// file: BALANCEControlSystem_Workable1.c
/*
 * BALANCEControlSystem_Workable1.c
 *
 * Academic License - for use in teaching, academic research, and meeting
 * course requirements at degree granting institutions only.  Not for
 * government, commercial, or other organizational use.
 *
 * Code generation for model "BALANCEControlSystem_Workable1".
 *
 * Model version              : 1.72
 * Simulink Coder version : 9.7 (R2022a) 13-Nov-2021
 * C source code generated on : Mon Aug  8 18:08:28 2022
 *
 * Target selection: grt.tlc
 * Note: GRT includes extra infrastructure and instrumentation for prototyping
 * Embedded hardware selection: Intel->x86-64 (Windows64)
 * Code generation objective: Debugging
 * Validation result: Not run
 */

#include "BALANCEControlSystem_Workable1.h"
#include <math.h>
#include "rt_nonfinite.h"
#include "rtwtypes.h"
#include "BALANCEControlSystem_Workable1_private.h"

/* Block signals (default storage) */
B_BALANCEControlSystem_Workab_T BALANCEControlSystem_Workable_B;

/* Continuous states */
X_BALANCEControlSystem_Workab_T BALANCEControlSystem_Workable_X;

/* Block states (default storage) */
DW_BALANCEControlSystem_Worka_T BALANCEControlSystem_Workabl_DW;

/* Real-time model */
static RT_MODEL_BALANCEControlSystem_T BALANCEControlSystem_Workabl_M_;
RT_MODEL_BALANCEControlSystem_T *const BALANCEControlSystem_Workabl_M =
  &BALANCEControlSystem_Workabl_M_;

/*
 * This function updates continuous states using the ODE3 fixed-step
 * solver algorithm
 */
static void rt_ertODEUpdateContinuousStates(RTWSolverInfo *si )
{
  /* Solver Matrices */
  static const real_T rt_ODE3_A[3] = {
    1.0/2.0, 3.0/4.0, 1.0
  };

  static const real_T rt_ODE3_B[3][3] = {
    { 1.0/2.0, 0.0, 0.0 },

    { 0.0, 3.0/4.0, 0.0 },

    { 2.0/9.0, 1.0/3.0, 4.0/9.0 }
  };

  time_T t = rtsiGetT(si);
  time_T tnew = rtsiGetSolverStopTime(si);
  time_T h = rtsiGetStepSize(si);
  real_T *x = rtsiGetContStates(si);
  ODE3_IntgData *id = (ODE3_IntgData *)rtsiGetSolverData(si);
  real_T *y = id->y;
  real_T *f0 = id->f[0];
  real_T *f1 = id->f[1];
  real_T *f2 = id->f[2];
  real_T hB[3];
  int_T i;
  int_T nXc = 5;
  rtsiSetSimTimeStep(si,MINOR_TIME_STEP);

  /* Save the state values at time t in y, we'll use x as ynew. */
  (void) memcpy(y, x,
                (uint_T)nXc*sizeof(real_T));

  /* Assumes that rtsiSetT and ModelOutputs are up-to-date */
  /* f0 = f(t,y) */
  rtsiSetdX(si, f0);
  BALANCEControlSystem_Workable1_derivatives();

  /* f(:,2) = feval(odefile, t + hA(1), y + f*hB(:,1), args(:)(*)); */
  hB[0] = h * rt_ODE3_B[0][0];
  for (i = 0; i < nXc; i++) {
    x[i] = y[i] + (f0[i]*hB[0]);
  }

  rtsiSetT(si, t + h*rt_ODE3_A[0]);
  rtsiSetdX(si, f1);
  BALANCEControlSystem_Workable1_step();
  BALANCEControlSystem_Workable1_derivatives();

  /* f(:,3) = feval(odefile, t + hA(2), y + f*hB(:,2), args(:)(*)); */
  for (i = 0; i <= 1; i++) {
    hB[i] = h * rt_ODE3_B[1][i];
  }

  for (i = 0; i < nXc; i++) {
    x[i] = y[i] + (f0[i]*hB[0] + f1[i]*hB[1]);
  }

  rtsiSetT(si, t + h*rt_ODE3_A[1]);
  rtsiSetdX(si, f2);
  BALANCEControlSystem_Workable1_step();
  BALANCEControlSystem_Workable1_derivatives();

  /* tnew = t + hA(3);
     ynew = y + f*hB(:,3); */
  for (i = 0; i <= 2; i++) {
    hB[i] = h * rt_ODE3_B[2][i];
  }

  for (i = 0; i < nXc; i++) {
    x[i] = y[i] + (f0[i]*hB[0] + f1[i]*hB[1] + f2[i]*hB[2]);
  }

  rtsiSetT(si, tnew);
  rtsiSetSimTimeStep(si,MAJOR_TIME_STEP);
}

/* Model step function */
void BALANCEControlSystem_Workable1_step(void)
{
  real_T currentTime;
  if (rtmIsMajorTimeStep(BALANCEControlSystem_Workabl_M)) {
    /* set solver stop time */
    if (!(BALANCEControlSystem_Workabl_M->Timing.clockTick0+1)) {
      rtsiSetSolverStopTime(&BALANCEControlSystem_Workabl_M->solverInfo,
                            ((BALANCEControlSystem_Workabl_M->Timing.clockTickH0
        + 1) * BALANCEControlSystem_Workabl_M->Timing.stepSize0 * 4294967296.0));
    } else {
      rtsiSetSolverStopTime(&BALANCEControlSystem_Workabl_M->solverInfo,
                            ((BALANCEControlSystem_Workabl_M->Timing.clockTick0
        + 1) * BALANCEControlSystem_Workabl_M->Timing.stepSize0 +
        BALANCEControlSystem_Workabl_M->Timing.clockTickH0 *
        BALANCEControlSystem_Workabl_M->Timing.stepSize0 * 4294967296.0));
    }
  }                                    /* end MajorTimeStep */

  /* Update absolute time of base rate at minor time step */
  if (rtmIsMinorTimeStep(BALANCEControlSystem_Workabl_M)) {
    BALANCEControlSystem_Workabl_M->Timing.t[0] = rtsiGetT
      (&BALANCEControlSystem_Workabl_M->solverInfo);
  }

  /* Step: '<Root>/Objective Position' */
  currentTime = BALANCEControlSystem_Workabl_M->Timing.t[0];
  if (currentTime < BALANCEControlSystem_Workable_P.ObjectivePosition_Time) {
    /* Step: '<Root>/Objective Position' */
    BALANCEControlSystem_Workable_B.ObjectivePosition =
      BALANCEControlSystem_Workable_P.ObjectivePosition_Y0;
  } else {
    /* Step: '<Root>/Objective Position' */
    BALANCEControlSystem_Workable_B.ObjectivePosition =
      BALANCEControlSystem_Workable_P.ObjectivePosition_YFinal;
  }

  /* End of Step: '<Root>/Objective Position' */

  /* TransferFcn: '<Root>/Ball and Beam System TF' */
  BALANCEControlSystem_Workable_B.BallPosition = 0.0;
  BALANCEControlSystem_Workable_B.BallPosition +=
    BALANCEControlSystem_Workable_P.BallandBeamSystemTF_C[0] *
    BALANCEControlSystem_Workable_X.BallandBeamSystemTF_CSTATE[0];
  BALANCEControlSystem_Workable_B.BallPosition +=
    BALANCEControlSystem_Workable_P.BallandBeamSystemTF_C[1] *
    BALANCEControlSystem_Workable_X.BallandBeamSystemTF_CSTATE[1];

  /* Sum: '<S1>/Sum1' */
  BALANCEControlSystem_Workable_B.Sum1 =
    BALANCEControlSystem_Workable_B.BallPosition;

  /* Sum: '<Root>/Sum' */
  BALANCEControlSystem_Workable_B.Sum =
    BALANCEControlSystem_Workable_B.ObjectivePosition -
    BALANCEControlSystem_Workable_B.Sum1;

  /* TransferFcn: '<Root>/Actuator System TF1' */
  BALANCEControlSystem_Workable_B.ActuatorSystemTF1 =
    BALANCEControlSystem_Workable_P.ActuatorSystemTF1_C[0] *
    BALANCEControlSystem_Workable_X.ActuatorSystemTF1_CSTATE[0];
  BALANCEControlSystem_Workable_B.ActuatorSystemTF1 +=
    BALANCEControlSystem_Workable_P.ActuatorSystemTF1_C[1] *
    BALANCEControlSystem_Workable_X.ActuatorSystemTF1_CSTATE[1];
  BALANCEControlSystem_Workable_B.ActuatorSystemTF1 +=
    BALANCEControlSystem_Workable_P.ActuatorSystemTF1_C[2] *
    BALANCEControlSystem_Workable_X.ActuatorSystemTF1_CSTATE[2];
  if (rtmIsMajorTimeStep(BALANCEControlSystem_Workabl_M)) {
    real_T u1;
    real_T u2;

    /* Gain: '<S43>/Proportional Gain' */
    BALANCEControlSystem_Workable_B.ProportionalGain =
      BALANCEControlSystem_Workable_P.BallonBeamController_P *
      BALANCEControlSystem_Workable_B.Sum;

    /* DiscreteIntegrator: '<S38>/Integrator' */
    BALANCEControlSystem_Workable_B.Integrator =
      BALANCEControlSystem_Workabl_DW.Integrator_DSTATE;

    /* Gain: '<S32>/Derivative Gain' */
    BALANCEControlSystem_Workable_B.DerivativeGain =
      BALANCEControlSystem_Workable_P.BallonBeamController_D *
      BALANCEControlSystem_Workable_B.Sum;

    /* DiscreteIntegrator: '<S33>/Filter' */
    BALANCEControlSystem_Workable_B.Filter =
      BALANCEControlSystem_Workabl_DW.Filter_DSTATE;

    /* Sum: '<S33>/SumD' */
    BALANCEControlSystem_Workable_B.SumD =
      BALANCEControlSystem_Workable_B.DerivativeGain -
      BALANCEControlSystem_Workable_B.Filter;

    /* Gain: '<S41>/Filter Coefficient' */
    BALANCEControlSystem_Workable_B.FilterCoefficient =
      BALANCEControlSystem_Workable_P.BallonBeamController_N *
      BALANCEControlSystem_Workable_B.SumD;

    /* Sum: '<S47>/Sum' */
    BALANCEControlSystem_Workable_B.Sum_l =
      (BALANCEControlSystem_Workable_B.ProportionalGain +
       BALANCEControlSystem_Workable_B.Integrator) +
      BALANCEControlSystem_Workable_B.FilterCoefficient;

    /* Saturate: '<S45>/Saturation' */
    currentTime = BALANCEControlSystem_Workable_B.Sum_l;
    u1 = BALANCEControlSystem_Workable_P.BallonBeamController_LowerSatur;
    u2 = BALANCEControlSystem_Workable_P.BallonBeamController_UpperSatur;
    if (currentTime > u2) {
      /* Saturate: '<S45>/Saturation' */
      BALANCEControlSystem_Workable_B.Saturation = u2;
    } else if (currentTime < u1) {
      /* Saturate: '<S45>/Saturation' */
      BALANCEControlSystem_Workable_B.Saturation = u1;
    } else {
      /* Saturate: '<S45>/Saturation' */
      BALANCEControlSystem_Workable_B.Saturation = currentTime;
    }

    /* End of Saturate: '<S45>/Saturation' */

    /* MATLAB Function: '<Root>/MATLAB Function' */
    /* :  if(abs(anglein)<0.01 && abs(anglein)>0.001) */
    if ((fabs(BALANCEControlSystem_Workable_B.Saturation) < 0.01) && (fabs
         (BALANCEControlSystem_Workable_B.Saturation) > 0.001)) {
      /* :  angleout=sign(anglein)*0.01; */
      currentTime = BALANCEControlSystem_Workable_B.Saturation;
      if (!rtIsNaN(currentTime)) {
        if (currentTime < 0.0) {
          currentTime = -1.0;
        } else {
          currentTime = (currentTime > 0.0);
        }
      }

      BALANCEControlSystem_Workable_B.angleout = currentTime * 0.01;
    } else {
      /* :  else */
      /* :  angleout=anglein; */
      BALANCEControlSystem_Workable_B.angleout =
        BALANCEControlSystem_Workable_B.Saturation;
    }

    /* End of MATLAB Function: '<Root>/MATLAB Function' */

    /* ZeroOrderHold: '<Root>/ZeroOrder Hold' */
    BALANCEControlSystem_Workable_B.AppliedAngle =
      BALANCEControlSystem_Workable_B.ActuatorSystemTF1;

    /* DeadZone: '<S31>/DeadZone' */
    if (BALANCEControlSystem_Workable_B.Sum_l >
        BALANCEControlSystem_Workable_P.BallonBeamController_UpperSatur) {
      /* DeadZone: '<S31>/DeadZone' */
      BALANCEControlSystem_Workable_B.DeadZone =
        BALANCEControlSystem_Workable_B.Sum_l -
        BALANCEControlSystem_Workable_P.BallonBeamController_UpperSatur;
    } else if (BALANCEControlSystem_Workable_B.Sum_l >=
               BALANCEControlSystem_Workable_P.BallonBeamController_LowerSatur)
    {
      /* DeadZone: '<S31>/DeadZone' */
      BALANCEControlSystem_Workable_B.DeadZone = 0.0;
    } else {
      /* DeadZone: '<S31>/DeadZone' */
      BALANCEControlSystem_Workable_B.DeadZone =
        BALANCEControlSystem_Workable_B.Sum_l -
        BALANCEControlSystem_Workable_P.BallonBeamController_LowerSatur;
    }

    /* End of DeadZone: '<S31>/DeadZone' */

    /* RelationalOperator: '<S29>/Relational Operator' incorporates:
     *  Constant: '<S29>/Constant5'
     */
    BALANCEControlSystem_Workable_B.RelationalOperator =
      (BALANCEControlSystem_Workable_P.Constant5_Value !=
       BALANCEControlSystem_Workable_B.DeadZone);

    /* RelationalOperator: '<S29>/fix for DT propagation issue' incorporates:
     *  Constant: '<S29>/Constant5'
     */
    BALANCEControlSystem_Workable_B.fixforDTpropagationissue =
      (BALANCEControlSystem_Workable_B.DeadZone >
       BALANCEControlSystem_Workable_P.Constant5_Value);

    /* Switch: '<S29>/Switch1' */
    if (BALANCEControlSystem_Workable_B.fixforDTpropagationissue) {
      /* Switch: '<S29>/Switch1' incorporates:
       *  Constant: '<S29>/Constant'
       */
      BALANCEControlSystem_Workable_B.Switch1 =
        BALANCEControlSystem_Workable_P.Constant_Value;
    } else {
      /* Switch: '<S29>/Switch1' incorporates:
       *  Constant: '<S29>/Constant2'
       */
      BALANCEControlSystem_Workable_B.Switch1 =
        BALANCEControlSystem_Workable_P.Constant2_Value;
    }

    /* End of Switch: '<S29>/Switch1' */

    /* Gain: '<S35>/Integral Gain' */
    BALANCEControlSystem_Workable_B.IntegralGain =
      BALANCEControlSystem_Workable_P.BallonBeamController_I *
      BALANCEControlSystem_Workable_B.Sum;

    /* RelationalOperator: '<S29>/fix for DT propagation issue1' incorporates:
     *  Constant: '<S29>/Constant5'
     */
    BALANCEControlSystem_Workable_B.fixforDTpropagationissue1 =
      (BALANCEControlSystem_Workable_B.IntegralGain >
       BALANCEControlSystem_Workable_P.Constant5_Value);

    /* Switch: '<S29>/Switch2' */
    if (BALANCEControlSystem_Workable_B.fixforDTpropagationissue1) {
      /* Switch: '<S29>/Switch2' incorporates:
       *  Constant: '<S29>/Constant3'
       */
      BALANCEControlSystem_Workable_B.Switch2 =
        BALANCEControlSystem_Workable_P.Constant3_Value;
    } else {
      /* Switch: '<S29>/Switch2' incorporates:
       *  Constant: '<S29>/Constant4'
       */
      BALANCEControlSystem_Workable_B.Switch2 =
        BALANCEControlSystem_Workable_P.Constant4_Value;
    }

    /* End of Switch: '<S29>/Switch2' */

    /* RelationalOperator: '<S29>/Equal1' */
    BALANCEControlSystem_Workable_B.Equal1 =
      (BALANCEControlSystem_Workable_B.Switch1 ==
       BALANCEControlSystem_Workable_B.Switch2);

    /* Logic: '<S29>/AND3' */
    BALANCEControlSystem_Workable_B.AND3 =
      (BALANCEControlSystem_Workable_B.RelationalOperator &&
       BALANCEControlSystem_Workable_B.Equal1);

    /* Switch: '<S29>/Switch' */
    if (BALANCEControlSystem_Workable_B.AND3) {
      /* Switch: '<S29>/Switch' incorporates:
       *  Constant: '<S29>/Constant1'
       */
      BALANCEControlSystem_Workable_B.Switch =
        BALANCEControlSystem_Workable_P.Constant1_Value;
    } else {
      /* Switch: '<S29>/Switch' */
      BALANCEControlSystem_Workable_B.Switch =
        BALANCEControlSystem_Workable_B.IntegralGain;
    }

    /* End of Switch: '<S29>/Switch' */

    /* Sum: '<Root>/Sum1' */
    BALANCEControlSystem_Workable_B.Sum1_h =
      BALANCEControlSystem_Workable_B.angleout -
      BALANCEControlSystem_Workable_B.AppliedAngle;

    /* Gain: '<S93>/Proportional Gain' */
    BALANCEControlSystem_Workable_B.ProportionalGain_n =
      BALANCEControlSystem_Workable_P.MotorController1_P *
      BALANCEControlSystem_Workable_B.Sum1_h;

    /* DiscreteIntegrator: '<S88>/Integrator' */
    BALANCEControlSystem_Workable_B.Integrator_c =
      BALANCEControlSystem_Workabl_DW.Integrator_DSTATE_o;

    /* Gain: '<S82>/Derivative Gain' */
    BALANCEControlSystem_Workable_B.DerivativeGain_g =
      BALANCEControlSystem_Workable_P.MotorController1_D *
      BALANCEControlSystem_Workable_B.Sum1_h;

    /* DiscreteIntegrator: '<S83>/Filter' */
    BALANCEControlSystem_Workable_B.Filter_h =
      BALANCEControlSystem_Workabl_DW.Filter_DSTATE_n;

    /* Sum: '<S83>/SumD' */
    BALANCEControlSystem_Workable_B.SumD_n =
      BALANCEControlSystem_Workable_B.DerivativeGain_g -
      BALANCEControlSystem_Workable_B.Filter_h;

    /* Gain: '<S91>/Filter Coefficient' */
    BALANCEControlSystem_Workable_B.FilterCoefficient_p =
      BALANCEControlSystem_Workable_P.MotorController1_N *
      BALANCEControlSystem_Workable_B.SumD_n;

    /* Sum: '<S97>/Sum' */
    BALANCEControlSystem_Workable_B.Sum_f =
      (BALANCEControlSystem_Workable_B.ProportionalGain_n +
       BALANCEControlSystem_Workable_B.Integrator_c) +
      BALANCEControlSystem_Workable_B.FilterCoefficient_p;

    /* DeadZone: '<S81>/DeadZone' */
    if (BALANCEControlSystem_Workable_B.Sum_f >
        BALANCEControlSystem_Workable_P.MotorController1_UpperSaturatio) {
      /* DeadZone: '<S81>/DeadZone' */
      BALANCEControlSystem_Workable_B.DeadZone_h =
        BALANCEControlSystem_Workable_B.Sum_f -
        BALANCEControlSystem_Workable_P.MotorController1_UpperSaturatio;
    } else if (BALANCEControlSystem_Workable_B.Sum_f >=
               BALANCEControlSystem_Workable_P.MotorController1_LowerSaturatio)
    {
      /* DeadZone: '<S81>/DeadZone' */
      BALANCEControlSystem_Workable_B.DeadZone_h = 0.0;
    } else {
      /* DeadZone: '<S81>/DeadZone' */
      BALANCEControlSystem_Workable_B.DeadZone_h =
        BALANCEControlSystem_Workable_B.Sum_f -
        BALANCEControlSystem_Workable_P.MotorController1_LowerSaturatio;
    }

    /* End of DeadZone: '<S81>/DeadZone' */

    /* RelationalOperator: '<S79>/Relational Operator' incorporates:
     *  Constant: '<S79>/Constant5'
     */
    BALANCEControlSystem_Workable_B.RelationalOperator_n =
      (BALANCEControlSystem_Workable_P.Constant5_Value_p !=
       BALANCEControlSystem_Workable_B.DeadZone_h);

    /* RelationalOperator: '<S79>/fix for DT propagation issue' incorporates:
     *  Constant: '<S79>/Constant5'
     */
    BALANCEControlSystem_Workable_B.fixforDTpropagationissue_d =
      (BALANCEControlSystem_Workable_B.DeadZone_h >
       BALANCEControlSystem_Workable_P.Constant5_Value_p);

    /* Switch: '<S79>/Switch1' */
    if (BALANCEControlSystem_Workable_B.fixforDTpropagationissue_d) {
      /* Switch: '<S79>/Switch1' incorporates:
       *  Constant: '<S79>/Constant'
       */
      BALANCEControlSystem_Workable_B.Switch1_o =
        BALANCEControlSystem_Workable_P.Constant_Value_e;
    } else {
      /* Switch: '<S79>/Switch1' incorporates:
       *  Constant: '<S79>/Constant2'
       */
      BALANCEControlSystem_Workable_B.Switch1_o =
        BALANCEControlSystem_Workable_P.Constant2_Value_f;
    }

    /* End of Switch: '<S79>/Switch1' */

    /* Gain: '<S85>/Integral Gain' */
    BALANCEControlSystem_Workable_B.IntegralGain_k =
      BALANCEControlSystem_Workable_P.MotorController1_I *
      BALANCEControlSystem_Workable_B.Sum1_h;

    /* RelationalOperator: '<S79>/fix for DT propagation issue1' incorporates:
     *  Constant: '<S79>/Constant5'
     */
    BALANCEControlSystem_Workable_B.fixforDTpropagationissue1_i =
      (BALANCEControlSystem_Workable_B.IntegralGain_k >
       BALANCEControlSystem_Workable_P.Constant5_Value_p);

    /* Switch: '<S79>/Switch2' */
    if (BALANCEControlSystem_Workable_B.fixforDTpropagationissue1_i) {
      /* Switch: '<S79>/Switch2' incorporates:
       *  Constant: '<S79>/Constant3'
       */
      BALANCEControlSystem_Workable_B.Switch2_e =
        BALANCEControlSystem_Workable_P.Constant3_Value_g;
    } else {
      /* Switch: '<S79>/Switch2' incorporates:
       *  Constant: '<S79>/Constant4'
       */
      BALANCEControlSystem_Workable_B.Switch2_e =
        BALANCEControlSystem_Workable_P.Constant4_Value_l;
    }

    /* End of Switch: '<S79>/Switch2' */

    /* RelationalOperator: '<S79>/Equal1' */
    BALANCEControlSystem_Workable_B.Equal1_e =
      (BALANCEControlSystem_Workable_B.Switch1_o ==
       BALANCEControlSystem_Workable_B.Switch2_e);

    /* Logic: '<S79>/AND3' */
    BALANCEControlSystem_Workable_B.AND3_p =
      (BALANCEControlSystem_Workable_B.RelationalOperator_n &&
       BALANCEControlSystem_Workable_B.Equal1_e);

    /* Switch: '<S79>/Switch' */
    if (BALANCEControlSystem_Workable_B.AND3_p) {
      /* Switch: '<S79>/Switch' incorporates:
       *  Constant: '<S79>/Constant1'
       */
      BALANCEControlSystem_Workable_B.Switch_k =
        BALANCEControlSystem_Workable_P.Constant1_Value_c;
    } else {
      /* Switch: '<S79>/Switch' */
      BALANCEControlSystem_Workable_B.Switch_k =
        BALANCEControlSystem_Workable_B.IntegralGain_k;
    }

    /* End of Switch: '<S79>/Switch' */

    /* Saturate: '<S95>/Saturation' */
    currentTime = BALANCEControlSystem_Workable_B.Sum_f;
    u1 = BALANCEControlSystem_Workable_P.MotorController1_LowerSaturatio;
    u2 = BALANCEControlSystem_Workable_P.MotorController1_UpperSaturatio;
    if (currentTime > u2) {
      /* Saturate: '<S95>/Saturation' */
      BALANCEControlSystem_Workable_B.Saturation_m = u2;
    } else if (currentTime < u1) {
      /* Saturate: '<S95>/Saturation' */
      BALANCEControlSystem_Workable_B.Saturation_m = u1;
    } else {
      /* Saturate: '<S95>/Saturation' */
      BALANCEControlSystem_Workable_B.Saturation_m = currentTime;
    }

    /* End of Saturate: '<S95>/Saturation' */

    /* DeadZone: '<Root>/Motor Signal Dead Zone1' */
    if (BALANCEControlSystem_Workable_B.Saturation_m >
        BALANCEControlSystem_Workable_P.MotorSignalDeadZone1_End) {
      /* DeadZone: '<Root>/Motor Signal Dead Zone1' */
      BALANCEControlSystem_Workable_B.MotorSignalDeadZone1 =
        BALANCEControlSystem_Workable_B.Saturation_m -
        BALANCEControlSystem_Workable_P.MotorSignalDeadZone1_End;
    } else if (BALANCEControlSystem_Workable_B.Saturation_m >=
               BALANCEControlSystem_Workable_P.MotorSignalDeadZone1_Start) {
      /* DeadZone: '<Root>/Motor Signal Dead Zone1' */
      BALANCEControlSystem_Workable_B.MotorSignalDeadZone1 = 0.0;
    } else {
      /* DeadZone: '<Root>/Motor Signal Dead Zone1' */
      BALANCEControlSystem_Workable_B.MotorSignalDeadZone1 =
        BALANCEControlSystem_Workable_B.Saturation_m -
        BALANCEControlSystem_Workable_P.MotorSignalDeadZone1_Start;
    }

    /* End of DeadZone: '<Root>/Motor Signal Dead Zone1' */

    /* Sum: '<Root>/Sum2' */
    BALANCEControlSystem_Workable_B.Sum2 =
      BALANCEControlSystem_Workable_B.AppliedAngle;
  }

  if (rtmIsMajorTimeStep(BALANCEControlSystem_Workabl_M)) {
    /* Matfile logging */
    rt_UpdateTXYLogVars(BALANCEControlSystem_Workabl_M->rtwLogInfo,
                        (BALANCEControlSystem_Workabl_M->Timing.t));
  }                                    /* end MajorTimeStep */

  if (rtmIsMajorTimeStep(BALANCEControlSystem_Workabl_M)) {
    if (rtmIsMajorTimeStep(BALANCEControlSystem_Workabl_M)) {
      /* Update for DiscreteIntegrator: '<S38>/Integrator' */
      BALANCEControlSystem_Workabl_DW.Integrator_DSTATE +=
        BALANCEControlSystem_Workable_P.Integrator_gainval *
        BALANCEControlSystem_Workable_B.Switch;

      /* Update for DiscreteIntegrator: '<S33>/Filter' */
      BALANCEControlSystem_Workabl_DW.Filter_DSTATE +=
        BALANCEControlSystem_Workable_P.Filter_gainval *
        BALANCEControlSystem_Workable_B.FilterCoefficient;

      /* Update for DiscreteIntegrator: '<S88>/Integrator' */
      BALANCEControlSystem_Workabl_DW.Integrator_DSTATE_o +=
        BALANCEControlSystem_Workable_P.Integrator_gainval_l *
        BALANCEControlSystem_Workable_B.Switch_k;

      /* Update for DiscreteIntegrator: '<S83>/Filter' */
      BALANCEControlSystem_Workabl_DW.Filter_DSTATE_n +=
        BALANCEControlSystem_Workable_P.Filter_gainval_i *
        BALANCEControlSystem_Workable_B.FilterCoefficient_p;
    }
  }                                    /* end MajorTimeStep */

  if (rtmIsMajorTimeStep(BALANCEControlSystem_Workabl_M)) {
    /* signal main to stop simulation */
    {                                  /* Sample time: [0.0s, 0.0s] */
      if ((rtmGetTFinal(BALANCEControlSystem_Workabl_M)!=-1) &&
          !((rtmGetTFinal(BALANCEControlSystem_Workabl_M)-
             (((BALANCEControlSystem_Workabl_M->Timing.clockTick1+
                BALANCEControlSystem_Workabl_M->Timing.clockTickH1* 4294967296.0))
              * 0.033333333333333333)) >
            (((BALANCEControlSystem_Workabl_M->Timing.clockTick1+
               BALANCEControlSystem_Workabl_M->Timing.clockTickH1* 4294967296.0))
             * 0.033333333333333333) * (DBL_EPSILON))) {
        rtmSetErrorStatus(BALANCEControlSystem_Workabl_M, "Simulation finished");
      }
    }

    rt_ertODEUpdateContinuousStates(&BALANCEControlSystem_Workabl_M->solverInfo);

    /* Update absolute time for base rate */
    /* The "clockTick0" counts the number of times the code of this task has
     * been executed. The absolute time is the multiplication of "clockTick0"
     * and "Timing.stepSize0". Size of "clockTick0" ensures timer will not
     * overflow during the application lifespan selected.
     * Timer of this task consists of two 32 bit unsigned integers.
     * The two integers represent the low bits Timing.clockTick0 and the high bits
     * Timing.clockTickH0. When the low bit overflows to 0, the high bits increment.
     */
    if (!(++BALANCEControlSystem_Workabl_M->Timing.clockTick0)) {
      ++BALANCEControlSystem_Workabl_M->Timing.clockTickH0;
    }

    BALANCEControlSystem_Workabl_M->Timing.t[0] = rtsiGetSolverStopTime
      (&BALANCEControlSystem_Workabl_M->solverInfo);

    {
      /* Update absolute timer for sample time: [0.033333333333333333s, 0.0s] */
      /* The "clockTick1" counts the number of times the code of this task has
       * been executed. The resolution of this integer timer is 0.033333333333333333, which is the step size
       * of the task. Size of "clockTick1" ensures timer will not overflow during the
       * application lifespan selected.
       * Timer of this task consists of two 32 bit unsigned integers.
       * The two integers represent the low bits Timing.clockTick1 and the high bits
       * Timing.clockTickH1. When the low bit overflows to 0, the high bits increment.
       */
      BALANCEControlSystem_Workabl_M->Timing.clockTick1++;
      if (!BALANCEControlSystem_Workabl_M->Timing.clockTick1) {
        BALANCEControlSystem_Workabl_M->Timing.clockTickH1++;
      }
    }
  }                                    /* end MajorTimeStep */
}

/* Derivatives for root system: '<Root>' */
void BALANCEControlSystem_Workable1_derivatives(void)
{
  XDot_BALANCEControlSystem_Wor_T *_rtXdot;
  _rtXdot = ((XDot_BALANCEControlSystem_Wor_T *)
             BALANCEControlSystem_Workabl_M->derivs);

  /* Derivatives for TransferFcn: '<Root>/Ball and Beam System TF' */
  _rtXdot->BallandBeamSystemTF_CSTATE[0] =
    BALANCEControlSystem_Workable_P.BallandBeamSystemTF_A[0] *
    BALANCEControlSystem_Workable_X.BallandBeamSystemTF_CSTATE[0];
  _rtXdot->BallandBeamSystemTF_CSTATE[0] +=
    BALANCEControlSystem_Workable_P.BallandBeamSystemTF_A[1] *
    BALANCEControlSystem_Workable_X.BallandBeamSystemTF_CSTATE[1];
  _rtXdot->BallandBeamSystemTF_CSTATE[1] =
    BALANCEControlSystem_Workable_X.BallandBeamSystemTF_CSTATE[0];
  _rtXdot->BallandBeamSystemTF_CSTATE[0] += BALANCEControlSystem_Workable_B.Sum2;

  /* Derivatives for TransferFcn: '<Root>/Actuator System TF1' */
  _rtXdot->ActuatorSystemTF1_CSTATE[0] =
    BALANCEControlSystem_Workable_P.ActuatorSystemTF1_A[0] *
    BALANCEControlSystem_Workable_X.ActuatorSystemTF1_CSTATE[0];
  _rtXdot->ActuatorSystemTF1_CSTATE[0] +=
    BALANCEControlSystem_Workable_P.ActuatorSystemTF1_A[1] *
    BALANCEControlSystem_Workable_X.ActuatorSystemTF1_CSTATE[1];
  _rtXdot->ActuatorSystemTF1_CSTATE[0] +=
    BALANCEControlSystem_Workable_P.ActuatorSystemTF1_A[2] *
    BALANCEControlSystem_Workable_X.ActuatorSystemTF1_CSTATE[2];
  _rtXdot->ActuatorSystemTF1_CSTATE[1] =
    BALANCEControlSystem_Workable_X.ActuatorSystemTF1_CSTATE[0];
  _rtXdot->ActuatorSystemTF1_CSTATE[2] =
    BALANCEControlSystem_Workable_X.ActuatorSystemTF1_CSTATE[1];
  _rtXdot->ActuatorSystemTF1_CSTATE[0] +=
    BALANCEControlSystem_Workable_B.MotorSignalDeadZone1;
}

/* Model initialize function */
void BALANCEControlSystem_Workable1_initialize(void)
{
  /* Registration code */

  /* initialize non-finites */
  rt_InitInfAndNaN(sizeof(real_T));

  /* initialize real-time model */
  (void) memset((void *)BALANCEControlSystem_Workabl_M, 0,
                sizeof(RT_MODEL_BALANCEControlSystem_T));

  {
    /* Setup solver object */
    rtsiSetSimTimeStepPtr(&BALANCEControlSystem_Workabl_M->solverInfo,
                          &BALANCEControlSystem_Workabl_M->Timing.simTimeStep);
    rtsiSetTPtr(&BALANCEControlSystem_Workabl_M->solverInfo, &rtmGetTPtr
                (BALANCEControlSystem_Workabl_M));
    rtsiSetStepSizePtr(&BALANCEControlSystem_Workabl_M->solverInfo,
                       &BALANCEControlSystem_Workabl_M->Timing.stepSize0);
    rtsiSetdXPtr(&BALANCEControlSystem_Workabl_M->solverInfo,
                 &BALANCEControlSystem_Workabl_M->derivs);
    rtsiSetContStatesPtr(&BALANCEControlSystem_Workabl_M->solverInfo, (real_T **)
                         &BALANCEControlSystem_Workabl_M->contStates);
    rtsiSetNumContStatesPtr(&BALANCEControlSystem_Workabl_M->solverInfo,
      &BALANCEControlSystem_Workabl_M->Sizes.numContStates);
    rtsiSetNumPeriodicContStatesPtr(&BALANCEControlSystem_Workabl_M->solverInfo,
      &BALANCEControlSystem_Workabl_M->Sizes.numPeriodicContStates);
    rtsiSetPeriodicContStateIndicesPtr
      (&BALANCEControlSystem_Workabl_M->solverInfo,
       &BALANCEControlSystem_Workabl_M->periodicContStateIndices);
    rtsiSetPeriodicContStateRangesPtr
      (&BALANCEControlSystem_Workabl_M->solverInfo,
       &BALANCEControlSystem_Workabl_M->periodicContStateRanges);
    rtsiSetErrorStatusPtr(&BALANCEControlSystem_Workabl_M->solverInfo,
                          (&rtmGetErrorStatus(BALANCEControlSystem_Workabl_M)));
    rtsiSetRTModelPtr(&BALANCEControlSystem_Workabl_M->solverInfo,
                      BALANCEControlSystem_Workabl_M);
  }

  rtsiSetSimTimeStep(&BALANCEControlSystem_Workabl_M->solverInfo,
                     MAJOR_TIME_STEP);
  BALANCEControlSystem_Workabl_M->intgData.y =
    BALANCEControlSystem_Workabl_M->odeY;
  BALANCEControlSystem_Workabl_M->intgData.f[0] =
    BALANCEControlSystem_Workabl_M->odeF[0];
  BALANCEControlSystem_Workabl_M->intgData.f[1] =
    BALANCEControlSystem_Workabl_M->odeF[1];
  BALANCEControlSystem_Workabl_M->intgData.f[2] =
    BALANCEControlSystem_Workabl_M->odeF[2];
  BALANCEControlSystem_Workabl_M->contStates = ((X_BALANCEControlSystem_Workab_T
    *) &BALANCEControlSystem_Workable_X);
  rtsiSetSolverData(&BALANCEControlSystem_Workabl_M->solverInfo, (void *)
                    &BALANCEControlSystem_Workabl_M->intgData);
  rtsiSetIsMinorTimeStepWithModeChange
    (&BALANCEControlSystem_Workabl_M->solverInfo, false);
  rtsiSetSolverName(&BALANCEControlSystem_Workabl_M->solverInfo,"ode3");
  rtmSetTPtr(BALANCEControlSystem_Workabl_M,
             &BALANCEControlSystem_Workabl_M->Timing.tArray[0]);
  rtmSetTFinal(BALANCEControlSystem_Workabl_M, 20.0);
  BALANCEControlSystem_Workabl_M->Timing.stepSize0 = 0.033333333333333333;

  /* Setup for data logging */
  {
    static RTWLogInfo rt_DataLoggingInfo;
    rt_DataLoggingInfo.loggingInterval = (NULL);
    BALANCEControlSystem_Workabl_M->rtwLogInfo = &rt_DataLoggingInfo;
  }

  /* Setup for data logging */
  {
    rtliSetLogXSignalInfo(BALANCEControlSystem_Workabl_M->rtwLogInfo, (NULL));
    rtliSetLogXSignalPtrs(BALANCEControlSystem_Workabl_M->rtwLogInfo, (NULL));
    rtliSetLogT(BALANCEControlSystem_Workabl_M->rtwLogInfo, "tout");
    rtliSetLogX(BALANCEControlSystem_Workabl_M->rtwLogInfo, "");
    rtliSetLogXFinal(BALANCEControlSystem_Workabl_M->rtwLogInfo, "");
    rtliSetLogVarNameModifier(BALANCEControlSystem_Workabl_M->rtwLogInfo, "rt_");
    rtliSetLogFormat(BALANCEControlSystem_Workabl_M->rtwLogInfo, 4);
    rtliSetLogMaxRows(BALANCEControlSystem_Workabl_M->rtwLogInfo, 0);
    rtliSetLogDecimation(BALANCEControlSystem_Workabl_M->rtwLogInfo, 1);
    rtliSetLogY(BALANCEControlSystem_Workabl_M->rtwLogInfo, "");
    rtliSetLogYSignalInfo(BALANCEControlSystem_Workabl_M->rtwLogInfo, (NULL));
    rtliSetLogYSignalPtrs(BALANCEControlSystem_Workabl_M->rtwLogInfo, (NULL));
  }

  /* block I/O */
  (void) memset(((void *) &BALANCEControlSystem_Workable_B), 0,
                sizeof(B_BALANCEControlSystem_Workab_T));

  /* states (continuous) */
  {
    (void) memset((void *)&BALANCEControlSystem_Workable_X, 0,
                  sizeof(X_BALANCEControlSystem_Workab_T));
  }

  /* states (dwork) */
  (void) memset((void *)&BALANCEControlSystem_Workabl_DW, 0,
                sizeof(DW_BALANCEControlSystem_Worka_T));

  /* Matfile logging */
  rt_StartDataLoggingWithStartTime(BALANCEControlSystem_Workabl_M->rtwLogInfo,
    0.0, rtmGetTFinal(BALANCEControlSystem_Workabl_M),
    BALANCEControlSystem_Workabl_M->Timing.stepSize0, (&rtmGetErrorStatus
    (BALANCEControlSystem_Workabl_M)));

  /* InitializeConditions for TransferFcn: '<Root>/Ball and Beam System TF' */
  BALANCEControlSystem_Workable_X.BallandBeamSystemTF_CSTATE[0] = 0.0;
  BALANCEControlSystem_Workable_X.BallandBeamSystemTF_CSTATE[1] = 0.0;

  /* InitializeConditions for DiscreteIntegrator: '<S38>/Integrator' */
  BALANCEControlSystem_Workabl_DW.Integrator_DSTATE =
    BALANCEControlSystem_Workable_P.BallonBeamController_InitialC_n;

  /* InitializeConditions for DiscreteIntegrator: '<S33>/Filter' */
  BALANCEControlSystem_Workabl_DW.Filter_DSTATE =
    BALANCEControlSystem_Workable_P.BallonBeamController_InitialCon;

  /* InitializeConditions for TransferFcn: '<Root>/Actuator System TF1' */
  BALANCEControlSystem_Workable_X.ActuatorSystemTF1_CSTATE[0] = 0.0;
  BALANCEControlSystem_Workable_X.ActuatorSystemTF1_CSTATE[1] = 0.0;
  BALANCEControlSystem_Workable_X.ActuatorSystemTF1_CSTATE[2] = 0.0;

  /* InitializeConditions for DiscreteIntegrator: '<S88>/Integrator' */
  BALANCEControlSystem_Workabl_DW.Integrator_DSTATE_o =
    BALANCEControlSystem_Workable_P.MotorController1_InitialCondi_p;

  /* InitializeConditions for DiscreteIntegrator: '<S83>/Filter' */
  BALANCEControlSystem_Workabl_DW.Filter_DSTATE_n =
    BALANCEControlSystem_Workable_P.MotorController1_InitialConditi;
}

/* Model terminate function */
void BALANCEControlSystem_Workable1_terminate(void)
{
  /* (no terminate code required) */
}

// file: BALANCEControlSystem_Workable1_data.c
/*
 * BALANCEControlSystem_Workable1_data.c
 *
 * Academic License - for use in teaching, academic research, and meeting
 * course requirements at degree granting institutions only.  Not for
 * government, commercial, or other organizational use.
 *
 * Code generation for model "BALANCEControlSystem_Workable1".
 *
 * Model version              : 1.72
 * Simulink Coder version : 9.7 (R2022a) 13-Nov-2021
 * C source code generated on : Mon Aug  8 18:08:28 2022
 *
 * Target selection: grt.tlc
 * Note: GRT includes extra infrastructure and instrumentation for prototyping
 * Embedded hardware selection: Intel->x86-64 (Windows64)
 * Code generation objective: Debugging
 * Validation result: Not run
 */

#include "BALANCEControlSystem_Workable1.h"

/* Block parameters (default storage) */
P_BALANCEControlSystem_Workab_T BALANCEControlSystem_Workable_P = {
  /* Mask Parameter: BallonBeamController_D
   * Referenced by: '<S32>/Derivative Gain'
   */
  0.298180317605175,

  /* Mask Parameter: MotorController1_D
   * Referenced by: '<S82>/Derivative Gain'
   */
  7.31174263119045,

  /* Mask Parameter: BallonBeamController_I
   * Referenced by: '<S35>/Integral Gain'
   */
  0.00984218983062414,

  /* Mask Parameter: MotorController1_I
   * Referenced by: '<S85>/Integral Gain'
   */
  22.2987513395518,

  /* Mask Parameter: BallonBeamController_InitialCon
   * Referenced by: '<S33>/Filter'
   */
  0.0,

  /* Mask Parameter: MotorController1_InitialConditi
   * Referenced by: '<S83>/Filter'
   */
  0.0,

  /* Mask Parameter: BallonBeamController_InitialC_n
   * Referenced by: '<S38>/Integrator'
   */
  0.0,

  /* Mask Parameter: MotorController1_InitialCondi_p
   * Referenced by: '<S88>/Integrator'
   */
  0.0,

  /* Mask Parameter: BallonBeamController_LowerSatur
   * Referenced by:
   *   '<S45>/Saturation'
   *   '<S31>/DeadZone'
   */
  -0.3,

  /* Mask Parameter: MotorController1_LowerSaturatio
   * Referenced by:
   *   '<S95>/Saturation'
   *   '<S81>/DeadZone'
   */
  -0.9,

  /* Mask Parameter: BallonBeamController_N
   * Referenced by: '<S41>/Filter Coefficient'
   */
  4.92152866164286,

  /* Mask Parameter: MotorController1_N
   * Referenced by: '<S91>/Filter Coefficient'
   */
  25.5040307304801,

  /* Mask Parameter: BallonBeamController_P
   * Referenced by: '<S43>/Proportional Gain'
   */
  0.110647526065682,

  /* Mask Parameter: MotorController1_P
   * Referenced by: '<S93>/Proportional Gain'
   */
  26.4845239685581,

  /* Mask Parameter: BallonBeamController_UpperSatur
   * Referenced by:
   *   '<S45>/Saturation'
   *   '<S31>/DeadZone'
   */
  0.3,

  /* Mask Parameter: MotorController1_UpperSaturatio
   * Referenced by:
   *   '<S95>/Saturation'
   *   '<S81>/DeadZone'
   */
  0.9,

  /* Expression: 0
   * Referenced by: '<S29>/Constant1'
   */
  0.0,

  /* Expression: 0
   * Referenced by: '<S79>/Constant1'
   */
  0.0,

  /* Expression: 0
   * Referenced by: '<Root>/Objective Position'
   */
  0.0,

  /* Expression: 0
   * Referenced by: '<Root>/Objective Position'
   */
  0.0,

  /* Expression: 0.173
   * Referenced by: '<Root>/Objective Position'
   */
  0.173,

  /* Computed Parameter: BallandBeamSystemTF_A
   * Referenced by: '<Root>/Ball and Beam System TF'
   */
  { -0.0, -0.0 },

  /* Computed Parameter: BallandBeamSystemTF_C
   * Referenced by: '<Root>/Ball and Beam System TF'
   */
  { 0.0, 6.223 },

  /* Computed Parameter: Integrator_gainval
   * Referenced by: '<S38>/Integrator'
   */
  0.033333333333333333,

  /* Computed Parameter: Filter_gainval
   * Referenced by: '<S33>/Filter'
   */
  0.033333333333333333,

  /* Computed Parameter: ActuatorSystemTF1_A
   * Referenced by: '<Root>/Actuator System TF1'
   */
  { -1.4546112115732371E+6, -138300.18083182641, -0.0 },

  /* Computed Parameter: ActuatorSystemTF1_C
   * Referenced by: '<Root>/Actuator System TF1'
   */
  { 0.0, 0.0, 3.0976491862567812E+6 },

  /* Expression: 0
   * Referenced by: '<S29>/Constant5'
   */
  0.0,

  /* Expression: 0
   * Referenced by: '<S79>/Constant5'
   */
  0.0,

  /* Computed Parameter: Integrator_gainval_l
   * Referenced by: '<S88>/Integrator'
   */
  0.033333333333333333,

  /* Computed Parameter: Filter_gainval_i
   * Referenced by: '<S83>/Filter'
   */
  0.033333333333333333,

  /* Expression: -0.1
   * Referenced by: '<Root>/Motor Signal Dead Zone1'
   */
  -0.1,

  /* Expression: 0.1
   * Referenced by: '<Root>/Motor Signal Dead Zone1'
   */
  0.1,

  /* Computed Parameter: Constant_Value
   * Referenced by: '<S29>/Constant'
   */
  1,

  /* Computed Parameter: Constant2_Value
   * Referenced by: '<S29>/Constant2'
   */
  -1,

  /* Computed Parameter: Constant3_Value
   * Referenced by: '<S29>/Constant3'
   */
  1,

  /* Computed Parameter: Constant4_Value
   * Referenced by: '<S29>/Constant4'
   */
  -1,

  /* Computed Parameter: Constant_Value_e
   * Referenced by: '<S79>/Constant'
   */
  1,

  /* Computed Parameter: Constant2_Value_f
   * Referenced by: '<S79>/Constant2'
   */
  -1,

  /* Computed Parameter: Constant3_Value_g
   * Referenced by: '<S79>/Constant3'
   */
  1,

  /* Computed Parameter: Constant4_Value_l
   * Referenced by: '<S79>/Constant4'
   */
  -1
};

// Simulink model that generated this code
simulink model "BALANCEControlSystem_Workable1"  (R2022a)
settings: Solver=FixedStepAuto  StartTime=0.0  StopTime=20  RelTol=1e-3
libraries: simulink x3, slpidlib x2

== system BALANCEControlSystem_Workable1 ==
  note: Ball and Beam Plant
  note: Actuator Plant
  note: Actuator Controller
  note: Ball and Beam
      | Controller
  note: Acuator Control
  Abs : Abs  Commented=on  SaturateOnIntegerOverflow=off
  Actuator System TF1 : TransferFcn  Numerator=[0.01713]  Denominator=[5.53e-09 0.008044 0.0007648 0]
  BALANCE CV System : Subsystem
  Ball and Beam System TF : TransferFcn  Numerator=[6.223]  Denominator=[1 0 0]
  Ball on Beam Controller : slpidlib/PID Controller  Controller=PID  Form=Parallel  TimeDomain=Discrete-time  UseExternalTs=off  SampleTime=1/30  IntegratorMethod=Forward Euler  FilterMethod=Forward Euler  ControllerParametersSource=internal  P=0.110647526065682  I=0.00984218983062414  UseKiTs=off  D=0.298180317605175  N=4.92152866164286  UseFilter=on  TunerSelectOption=Transfer Function Based (PID Tuner App)  InitialConditionSource=internal  InitialConditionForIntegrator=0  InitialConditionForFilter=0  DifferentiatorICPrevScaledInput=0  ExternalReset=none  TrackingMode=off  Kt=1  LimitOutput=on  SatLimitsSource=internal  UpperSaturationLimit=0.3  LowerSaturationLimit=-0.3  LinearizeAsGain=off  AntiWindupMode=clamping  Kb=1  POutMin=[]  POutMax=[]  IOutMin=[]  IOutMax=[]  DOutMin=[]  DOutMax=[]  NOutMin=[]  NOutMax=[]  SumOutMin=[]  SumOutMax=[]  SaturationOutMin=[]  SaturationOutMax=[]  PParamMin=[]  PParamMax=[]  IParamMin=[]  IParamMax=[]  DParamMin=[]  DParamMax=[]  NParamMin=[]  NParamMax=[]  KbParamMin=[]  KbParamMax=[]  KtParamMin=[]  KtParamMax=[]  KbOutMin=[]  KbOutMax=[]  KtOutMin=[]  KtOutMax=[]  IntegratorOutMin=[]  IntegratorOutMax=[]  FilterOutMin=[]  FilterOutMax=[]  SumI1OutMin=[]  SumI1OutMax=[]  SumI2OutMin=[]  SumI2OutMax=[]  SumI3OutMin=[]  SumI3OutMax=[]  SumI4OutMin=[]  SumI4OutMax=[]  SumDOutMin=[]  SumDOutMax=[]  DifferentiatorOutMin=[]  DifferentiatorOutMax=[]  FilterDiffOutCoefMin=[]  FilterDiffOutCoefMax=[]  ReciprocalOutMin=[]  ReciprocalOutMax=[]  SumDenOutMin=[]  SumDenOutMax=[]  SumNumOutMin=[]  SumNumOutMax=[]  DivideOutMin=[]  DivideOutMax=[]  UdiffTsProdOutMin=[]  UdiffTsProdOutMax=[]  NTsProdOutMin=[]  NTsProdOutMax=[]  UintegralTsProdOutMin=[]  UintegralTsProdOutMax=[]  UngainTsProdOutMin=[]  UngainTsProdOutMax=[]  IntegratorContinuousStateAttributes=''  IntegratorStateMustResolveToSignalObject=off  IntegratorRTWStateStorageClass=Auto  FilterContinuousStateAttributes=''  FilterStateMustResolveToSignalObject=off  FilterRTWStateStorageClass=Auto  ParallelPVariant=InternalParameters  IdealPVariant=Disabled  IVariant=InternalParameters  DVariant=InternalParameters  IntegratorVariant=Discrete  SatVariant=Enabled  AWVariant=DiscClampingParallel  PCopyVariant=Disabled  TRVariant=Disabled  FdbkBlocksVariant=Forward  IdealPFdbkVariant=Disabled  SatFdbkVariant=Disabled  DerivativeFilterVariant=ForwardEulerFilter  NVariant=InternalParameters  NCopyVariant=Disabled  FilterICVariant=InternalICsFilter  IntegratorICVariant=InternalICs  ExternalResetVariant=Disabled  TRSumVariant=Passthrough  SumFdbkVariant=Disabled  SumVariant=Sum_PID  TsampFilterVariant=InternalTs  TsampNgainVariant=Passthrough  TsampIntegralVariant=Passthrough  ExternalSaturationOutDataTypeStr=Inherit: Same as second input  aMode=0
  MATLAB Function : MATLAB Function  TreatAsAtomicUnit=on
  Motor Controller1 : slpidlib/PID Controller  Controller=PID  Form=Parallel  TimeDomain=Discrete-time  UseExternalTs=off  SampleTime=1/30  IntegratorMethod=Forward Euler  FilterMethod=Forward Euler  ControllerParametersSource=internal  P=26.4845239685581  I=22.2987513395518  UseKiTs=off  D=7.31174263119045  N=25.5040307304801  UseFilter=on  TunerSelectOption=Transfer Function Based (PID Tuner App)  InitialConditionSource=internal  InitialConditionForIntegrator=0  InitialConditionForFilter=0  DifferentiatorICPrevScaledInput=0  ExternalReset=none  TrackingMode=off  Kt=1  LimitOutput=on  SatLimitsSource=internal  UpperSaturationLimit=0.9  LowerSaturationLimit=-0.9  LinearizeAsGain=off  AntiWindupMode=clamping  Kb=1  POutMin=[]  POutMax=[]  IOutMin=[]  IOutMax=[]  DOutMin=[]  DOutMax=[]  NOutMin=[]  NOutMax=[]  SumOutMin=[]  SumOutMax=[]  SaturationOutMin=[]  SaturationOutMax=[]  PParamMin=[]  PParamMax=[]  IParamMin=[]  IParamMax=[]  DParamMin=[]  DParamMax=[]  NParamMin=[]  NParamMax=[]  KbParamMin=[]  KbParamMax=[]  KtParamMin=[]  KtParamMax=[]  KbOutMin=[]  KbOutMax=[]  KtOutMin=[]  KtOutMax=[]  IntegratorOutMin=[]  IntegratorOutMax=[]  FilterOutMin=[]  FilterOutMax=[]  SumI1OutMin=[]  SumI1OutMax=[]  SumI2OutMin=[]  SumI2OutMax=[]  SumI3OutMin=[]  SumI3OutMax=[]  SumI4OutMin=[]  SumI4OutMax=[]  SumDOutMin=[]  SumDOutMax=[]  DifferentiatorOutMin=[]  DifferentiatorOutMax=[]  FilterDiffOutCoefMin=[]  FilterDiffOutCoefMax=[]  ReciprocalOutMin=[]  ReciprocalOutMax=[]  SumDenOutMin=[]  SumDenOutMax=[]  SumNumOutMin=[]  SumNumOutMax=[]  DivideOutMin=[]  DivideOutMax=[]  UdiffTsProdOutMin=[]  UdiffTsProdOutMax=[]  NTsProdOutMin=[]  NTsProdOutMax=[]  UintegralTsProdOutMin=[]  UintegralTsProdOutMax=[]  UngainTsProdOutMin=[]  UngainTsProdOutMax=[]  IntegratorContinuousStateAttributes=''  IntegratorStateMustResolveToSignalObject=off  IntegratorRTWStateStorageClass=Auto  FilterContinuousStateAttributes=''  FilterStateMustResolveToSignalObject=off  FilterRTWStateStorageClass=Auto  ParallelPVariant=InternalParameters  IdealPVariant=Disabled  IVariant=InternalParameters  DVariant=InternalParameters  IntegratorVariant=Discrete  SatVariant=Enabled  AWVariant=DiscClampingParallel  PCopyVariant=Disabled  TRVariant=Disabled  FdbkBlocksVariant=Forward  IdealPFdbkVariant=Disabled  SatFdbkVariant=Disabled  DerivativeFilterVariant=ForwardEulerFilter  NVariant=InternalParameters  NCopyVariant=Disabled  FilterICVariant=InternalICsFilter  IntegratorICVariant=InternalICs  ExternalResetVariant=Disabled  TRSumVariant=Passthrough  SumFdbkVariant=Disabled  SumVariant=Sum_PID  TsampFilterVariant=InternalTs  TsampNgainVariant=Passthrough  TsampIntegralVariant=Passthrough  ExternalSaturationOutDataTypeStr=Inherit: Same as second input  aMode=0
  Motor PWM : simulink/Discontinuities/PWM  Commented=on  DisableCoverage=on  Period=1  DisallowZeroDutyCycle=off  RunAtFixedTimeIntervals=off  SampleTime=0.1
  Motor Signal Dead Zone1 : DeadZone  LowerValue=-0.1  UpperValue=0.1
  "Motor Signal Zero-Order Hold " : ZeroOrderHold  SampleTime=-1
  Objective Position : Step  Time=0  After=0.173  SampleTime=0
  Scope : Scope  NumInputPorts=4
  Scope1 : Scope  Commented=on  NumInputPorts=2
  Sign : Signum  Commented=on
  Sum : Sum  Inputs=|+-
  Sum1 : Sum  Inputs=|+-
  Sum2 : Sum  Inputs=|++
  Waveform Generator : simulink/Sources/Waveform Generator  Commented=on  OutMin=[]  OutMax=[]  OutDataTypeStr=double  SelectedSignal=1  Signals=sin(0.001,3,1)  BlockNames=MultiportSwitch_d9878704260749e  SampleTime=0.1
  ZeroOrder Hold : ZeroOrderHold  SampleTime=-1
  wires:
  Objective Position/1 -> Scope/1, Sum/1
  BALANCE CV System/1(Ball Distance) -> Sum/2
  MATLAB Function/1(angleout) -> Scope/3, Sum1/1  "Objective Angle"
  Sum/1 -> Ball on Beam Controller/1
  Motor Controller1/1 -> Motor Signal Dead Zone1/1
  Motor Signal Dead Zone1/1 -> "Motor Signal Zero-Order Hold "/1
  Sum1/1 -> Motor Controller1/1
  Sign/1 -> Scope1/1  "Motor Direction"
  Motor PWM/1 -> Scope1/2
  Abs/1 -> Motor PWM/1
  "Motor Signal Zero-Order Hold "/1 -> Sign/1, Abs/1, Actuator System TF1/1
  Actuator System TF1/1 -> ZeroOrder Hold/1
  Sum2/1 -> Ball and Beam System TF/1
  Waveform Generator/1 -> Sum2/2  "Ball Disturbance"
  Ball and Beam System TF/1 -> BALANCE CV System/1(Ball Coordinates), Scope/2  "BallPosition"
  ZeroOrder Hold/1 -> Sum1/2, Scope/4, Sum2/1  "Applied Angle"
  Ball on Beam Controller/1 -> MATLAB Function/1(anglein)

== system BALANCEControlSystem_Workable1/BALANCE CV System ==
  Ball Coordinates : Inport
  Computer Vision Delay : Delay  Commented=through
  Sum1 : Sum  Inputs=|++
  Waveform Generator1 : simulink/Sources/Waveform Generator  Commented=on  OutMin=[]  OutMax=[]  OutDataTypeStr=double  SelectedSignal=1  Signals=sin(0.0001,3,1)  BlockNames=MultiportSwitch_425a7e8e9f63443  SampleTime=0.1
  Ball Distance : Outport
  wires:
  Waveform Generator1/1 -> Sum1/2  "Video Noise"
  Sum1/1 -> Computer Vision Delay/1
  Computer Vision Delay/1 -> Ball Distance/1
  Ball Coordinates/1 -> Sum1/1

== matlab function BALANCEControlSystem_Workable1/MATLAB Function ==
function angleout = disturb(anglein)

if(abs(anglein)<0.01 && abs(anglein)>0.001)
    angleout=sign(anglein)*0.01;
else
    angleout=anglein;
end
end
